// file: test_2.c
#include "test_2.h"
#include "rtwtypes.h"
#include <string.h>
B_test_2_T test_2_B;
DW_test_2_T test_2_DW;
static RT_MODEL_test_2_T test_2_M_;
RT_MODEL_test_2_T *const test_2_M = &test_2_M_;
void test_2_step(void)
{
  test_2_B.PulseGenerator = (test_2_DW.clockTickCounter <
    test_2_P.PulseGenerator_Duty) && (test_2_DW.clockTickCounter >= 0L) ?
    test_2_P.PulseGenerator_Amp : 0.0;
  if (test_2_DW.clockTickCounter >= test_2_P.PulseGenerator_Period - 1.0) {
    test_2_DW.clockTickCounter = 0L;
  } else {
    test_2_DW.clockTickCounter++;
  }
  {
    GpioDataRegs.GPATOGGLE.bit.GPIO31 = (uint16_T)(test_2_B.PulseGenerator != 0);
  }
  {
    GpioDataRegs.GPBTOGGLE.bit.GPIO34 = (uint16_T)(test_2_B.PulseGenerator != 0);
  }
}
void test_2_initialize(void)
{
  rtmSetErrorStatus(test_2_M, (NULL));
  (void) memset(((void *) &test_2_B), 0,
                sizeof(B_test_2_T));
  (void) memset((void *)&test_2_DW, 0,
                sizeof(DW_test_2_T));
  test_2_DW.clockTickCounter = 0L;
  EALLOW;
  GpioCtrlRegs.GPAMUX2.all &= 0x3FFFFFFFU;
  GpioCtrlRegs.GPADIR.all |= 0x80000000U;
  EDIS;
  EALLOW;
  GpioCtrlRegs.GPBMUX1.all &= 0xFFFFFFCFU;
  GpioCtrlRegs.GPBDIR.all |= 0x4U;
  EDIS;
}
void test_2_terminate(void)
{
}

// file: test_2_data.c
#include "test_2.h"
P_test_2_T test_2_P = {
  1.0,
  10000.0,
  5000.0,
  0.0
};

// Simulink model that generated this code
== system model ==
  DigitalOutput#1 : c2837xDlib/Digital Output  <- 1: PulseGenerator
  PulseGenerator : DiscretePulseGenerator  Period=1  PulseWidth=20
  DigitalOutput#2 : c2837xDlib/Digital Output  <- 1: PulseGenerator
